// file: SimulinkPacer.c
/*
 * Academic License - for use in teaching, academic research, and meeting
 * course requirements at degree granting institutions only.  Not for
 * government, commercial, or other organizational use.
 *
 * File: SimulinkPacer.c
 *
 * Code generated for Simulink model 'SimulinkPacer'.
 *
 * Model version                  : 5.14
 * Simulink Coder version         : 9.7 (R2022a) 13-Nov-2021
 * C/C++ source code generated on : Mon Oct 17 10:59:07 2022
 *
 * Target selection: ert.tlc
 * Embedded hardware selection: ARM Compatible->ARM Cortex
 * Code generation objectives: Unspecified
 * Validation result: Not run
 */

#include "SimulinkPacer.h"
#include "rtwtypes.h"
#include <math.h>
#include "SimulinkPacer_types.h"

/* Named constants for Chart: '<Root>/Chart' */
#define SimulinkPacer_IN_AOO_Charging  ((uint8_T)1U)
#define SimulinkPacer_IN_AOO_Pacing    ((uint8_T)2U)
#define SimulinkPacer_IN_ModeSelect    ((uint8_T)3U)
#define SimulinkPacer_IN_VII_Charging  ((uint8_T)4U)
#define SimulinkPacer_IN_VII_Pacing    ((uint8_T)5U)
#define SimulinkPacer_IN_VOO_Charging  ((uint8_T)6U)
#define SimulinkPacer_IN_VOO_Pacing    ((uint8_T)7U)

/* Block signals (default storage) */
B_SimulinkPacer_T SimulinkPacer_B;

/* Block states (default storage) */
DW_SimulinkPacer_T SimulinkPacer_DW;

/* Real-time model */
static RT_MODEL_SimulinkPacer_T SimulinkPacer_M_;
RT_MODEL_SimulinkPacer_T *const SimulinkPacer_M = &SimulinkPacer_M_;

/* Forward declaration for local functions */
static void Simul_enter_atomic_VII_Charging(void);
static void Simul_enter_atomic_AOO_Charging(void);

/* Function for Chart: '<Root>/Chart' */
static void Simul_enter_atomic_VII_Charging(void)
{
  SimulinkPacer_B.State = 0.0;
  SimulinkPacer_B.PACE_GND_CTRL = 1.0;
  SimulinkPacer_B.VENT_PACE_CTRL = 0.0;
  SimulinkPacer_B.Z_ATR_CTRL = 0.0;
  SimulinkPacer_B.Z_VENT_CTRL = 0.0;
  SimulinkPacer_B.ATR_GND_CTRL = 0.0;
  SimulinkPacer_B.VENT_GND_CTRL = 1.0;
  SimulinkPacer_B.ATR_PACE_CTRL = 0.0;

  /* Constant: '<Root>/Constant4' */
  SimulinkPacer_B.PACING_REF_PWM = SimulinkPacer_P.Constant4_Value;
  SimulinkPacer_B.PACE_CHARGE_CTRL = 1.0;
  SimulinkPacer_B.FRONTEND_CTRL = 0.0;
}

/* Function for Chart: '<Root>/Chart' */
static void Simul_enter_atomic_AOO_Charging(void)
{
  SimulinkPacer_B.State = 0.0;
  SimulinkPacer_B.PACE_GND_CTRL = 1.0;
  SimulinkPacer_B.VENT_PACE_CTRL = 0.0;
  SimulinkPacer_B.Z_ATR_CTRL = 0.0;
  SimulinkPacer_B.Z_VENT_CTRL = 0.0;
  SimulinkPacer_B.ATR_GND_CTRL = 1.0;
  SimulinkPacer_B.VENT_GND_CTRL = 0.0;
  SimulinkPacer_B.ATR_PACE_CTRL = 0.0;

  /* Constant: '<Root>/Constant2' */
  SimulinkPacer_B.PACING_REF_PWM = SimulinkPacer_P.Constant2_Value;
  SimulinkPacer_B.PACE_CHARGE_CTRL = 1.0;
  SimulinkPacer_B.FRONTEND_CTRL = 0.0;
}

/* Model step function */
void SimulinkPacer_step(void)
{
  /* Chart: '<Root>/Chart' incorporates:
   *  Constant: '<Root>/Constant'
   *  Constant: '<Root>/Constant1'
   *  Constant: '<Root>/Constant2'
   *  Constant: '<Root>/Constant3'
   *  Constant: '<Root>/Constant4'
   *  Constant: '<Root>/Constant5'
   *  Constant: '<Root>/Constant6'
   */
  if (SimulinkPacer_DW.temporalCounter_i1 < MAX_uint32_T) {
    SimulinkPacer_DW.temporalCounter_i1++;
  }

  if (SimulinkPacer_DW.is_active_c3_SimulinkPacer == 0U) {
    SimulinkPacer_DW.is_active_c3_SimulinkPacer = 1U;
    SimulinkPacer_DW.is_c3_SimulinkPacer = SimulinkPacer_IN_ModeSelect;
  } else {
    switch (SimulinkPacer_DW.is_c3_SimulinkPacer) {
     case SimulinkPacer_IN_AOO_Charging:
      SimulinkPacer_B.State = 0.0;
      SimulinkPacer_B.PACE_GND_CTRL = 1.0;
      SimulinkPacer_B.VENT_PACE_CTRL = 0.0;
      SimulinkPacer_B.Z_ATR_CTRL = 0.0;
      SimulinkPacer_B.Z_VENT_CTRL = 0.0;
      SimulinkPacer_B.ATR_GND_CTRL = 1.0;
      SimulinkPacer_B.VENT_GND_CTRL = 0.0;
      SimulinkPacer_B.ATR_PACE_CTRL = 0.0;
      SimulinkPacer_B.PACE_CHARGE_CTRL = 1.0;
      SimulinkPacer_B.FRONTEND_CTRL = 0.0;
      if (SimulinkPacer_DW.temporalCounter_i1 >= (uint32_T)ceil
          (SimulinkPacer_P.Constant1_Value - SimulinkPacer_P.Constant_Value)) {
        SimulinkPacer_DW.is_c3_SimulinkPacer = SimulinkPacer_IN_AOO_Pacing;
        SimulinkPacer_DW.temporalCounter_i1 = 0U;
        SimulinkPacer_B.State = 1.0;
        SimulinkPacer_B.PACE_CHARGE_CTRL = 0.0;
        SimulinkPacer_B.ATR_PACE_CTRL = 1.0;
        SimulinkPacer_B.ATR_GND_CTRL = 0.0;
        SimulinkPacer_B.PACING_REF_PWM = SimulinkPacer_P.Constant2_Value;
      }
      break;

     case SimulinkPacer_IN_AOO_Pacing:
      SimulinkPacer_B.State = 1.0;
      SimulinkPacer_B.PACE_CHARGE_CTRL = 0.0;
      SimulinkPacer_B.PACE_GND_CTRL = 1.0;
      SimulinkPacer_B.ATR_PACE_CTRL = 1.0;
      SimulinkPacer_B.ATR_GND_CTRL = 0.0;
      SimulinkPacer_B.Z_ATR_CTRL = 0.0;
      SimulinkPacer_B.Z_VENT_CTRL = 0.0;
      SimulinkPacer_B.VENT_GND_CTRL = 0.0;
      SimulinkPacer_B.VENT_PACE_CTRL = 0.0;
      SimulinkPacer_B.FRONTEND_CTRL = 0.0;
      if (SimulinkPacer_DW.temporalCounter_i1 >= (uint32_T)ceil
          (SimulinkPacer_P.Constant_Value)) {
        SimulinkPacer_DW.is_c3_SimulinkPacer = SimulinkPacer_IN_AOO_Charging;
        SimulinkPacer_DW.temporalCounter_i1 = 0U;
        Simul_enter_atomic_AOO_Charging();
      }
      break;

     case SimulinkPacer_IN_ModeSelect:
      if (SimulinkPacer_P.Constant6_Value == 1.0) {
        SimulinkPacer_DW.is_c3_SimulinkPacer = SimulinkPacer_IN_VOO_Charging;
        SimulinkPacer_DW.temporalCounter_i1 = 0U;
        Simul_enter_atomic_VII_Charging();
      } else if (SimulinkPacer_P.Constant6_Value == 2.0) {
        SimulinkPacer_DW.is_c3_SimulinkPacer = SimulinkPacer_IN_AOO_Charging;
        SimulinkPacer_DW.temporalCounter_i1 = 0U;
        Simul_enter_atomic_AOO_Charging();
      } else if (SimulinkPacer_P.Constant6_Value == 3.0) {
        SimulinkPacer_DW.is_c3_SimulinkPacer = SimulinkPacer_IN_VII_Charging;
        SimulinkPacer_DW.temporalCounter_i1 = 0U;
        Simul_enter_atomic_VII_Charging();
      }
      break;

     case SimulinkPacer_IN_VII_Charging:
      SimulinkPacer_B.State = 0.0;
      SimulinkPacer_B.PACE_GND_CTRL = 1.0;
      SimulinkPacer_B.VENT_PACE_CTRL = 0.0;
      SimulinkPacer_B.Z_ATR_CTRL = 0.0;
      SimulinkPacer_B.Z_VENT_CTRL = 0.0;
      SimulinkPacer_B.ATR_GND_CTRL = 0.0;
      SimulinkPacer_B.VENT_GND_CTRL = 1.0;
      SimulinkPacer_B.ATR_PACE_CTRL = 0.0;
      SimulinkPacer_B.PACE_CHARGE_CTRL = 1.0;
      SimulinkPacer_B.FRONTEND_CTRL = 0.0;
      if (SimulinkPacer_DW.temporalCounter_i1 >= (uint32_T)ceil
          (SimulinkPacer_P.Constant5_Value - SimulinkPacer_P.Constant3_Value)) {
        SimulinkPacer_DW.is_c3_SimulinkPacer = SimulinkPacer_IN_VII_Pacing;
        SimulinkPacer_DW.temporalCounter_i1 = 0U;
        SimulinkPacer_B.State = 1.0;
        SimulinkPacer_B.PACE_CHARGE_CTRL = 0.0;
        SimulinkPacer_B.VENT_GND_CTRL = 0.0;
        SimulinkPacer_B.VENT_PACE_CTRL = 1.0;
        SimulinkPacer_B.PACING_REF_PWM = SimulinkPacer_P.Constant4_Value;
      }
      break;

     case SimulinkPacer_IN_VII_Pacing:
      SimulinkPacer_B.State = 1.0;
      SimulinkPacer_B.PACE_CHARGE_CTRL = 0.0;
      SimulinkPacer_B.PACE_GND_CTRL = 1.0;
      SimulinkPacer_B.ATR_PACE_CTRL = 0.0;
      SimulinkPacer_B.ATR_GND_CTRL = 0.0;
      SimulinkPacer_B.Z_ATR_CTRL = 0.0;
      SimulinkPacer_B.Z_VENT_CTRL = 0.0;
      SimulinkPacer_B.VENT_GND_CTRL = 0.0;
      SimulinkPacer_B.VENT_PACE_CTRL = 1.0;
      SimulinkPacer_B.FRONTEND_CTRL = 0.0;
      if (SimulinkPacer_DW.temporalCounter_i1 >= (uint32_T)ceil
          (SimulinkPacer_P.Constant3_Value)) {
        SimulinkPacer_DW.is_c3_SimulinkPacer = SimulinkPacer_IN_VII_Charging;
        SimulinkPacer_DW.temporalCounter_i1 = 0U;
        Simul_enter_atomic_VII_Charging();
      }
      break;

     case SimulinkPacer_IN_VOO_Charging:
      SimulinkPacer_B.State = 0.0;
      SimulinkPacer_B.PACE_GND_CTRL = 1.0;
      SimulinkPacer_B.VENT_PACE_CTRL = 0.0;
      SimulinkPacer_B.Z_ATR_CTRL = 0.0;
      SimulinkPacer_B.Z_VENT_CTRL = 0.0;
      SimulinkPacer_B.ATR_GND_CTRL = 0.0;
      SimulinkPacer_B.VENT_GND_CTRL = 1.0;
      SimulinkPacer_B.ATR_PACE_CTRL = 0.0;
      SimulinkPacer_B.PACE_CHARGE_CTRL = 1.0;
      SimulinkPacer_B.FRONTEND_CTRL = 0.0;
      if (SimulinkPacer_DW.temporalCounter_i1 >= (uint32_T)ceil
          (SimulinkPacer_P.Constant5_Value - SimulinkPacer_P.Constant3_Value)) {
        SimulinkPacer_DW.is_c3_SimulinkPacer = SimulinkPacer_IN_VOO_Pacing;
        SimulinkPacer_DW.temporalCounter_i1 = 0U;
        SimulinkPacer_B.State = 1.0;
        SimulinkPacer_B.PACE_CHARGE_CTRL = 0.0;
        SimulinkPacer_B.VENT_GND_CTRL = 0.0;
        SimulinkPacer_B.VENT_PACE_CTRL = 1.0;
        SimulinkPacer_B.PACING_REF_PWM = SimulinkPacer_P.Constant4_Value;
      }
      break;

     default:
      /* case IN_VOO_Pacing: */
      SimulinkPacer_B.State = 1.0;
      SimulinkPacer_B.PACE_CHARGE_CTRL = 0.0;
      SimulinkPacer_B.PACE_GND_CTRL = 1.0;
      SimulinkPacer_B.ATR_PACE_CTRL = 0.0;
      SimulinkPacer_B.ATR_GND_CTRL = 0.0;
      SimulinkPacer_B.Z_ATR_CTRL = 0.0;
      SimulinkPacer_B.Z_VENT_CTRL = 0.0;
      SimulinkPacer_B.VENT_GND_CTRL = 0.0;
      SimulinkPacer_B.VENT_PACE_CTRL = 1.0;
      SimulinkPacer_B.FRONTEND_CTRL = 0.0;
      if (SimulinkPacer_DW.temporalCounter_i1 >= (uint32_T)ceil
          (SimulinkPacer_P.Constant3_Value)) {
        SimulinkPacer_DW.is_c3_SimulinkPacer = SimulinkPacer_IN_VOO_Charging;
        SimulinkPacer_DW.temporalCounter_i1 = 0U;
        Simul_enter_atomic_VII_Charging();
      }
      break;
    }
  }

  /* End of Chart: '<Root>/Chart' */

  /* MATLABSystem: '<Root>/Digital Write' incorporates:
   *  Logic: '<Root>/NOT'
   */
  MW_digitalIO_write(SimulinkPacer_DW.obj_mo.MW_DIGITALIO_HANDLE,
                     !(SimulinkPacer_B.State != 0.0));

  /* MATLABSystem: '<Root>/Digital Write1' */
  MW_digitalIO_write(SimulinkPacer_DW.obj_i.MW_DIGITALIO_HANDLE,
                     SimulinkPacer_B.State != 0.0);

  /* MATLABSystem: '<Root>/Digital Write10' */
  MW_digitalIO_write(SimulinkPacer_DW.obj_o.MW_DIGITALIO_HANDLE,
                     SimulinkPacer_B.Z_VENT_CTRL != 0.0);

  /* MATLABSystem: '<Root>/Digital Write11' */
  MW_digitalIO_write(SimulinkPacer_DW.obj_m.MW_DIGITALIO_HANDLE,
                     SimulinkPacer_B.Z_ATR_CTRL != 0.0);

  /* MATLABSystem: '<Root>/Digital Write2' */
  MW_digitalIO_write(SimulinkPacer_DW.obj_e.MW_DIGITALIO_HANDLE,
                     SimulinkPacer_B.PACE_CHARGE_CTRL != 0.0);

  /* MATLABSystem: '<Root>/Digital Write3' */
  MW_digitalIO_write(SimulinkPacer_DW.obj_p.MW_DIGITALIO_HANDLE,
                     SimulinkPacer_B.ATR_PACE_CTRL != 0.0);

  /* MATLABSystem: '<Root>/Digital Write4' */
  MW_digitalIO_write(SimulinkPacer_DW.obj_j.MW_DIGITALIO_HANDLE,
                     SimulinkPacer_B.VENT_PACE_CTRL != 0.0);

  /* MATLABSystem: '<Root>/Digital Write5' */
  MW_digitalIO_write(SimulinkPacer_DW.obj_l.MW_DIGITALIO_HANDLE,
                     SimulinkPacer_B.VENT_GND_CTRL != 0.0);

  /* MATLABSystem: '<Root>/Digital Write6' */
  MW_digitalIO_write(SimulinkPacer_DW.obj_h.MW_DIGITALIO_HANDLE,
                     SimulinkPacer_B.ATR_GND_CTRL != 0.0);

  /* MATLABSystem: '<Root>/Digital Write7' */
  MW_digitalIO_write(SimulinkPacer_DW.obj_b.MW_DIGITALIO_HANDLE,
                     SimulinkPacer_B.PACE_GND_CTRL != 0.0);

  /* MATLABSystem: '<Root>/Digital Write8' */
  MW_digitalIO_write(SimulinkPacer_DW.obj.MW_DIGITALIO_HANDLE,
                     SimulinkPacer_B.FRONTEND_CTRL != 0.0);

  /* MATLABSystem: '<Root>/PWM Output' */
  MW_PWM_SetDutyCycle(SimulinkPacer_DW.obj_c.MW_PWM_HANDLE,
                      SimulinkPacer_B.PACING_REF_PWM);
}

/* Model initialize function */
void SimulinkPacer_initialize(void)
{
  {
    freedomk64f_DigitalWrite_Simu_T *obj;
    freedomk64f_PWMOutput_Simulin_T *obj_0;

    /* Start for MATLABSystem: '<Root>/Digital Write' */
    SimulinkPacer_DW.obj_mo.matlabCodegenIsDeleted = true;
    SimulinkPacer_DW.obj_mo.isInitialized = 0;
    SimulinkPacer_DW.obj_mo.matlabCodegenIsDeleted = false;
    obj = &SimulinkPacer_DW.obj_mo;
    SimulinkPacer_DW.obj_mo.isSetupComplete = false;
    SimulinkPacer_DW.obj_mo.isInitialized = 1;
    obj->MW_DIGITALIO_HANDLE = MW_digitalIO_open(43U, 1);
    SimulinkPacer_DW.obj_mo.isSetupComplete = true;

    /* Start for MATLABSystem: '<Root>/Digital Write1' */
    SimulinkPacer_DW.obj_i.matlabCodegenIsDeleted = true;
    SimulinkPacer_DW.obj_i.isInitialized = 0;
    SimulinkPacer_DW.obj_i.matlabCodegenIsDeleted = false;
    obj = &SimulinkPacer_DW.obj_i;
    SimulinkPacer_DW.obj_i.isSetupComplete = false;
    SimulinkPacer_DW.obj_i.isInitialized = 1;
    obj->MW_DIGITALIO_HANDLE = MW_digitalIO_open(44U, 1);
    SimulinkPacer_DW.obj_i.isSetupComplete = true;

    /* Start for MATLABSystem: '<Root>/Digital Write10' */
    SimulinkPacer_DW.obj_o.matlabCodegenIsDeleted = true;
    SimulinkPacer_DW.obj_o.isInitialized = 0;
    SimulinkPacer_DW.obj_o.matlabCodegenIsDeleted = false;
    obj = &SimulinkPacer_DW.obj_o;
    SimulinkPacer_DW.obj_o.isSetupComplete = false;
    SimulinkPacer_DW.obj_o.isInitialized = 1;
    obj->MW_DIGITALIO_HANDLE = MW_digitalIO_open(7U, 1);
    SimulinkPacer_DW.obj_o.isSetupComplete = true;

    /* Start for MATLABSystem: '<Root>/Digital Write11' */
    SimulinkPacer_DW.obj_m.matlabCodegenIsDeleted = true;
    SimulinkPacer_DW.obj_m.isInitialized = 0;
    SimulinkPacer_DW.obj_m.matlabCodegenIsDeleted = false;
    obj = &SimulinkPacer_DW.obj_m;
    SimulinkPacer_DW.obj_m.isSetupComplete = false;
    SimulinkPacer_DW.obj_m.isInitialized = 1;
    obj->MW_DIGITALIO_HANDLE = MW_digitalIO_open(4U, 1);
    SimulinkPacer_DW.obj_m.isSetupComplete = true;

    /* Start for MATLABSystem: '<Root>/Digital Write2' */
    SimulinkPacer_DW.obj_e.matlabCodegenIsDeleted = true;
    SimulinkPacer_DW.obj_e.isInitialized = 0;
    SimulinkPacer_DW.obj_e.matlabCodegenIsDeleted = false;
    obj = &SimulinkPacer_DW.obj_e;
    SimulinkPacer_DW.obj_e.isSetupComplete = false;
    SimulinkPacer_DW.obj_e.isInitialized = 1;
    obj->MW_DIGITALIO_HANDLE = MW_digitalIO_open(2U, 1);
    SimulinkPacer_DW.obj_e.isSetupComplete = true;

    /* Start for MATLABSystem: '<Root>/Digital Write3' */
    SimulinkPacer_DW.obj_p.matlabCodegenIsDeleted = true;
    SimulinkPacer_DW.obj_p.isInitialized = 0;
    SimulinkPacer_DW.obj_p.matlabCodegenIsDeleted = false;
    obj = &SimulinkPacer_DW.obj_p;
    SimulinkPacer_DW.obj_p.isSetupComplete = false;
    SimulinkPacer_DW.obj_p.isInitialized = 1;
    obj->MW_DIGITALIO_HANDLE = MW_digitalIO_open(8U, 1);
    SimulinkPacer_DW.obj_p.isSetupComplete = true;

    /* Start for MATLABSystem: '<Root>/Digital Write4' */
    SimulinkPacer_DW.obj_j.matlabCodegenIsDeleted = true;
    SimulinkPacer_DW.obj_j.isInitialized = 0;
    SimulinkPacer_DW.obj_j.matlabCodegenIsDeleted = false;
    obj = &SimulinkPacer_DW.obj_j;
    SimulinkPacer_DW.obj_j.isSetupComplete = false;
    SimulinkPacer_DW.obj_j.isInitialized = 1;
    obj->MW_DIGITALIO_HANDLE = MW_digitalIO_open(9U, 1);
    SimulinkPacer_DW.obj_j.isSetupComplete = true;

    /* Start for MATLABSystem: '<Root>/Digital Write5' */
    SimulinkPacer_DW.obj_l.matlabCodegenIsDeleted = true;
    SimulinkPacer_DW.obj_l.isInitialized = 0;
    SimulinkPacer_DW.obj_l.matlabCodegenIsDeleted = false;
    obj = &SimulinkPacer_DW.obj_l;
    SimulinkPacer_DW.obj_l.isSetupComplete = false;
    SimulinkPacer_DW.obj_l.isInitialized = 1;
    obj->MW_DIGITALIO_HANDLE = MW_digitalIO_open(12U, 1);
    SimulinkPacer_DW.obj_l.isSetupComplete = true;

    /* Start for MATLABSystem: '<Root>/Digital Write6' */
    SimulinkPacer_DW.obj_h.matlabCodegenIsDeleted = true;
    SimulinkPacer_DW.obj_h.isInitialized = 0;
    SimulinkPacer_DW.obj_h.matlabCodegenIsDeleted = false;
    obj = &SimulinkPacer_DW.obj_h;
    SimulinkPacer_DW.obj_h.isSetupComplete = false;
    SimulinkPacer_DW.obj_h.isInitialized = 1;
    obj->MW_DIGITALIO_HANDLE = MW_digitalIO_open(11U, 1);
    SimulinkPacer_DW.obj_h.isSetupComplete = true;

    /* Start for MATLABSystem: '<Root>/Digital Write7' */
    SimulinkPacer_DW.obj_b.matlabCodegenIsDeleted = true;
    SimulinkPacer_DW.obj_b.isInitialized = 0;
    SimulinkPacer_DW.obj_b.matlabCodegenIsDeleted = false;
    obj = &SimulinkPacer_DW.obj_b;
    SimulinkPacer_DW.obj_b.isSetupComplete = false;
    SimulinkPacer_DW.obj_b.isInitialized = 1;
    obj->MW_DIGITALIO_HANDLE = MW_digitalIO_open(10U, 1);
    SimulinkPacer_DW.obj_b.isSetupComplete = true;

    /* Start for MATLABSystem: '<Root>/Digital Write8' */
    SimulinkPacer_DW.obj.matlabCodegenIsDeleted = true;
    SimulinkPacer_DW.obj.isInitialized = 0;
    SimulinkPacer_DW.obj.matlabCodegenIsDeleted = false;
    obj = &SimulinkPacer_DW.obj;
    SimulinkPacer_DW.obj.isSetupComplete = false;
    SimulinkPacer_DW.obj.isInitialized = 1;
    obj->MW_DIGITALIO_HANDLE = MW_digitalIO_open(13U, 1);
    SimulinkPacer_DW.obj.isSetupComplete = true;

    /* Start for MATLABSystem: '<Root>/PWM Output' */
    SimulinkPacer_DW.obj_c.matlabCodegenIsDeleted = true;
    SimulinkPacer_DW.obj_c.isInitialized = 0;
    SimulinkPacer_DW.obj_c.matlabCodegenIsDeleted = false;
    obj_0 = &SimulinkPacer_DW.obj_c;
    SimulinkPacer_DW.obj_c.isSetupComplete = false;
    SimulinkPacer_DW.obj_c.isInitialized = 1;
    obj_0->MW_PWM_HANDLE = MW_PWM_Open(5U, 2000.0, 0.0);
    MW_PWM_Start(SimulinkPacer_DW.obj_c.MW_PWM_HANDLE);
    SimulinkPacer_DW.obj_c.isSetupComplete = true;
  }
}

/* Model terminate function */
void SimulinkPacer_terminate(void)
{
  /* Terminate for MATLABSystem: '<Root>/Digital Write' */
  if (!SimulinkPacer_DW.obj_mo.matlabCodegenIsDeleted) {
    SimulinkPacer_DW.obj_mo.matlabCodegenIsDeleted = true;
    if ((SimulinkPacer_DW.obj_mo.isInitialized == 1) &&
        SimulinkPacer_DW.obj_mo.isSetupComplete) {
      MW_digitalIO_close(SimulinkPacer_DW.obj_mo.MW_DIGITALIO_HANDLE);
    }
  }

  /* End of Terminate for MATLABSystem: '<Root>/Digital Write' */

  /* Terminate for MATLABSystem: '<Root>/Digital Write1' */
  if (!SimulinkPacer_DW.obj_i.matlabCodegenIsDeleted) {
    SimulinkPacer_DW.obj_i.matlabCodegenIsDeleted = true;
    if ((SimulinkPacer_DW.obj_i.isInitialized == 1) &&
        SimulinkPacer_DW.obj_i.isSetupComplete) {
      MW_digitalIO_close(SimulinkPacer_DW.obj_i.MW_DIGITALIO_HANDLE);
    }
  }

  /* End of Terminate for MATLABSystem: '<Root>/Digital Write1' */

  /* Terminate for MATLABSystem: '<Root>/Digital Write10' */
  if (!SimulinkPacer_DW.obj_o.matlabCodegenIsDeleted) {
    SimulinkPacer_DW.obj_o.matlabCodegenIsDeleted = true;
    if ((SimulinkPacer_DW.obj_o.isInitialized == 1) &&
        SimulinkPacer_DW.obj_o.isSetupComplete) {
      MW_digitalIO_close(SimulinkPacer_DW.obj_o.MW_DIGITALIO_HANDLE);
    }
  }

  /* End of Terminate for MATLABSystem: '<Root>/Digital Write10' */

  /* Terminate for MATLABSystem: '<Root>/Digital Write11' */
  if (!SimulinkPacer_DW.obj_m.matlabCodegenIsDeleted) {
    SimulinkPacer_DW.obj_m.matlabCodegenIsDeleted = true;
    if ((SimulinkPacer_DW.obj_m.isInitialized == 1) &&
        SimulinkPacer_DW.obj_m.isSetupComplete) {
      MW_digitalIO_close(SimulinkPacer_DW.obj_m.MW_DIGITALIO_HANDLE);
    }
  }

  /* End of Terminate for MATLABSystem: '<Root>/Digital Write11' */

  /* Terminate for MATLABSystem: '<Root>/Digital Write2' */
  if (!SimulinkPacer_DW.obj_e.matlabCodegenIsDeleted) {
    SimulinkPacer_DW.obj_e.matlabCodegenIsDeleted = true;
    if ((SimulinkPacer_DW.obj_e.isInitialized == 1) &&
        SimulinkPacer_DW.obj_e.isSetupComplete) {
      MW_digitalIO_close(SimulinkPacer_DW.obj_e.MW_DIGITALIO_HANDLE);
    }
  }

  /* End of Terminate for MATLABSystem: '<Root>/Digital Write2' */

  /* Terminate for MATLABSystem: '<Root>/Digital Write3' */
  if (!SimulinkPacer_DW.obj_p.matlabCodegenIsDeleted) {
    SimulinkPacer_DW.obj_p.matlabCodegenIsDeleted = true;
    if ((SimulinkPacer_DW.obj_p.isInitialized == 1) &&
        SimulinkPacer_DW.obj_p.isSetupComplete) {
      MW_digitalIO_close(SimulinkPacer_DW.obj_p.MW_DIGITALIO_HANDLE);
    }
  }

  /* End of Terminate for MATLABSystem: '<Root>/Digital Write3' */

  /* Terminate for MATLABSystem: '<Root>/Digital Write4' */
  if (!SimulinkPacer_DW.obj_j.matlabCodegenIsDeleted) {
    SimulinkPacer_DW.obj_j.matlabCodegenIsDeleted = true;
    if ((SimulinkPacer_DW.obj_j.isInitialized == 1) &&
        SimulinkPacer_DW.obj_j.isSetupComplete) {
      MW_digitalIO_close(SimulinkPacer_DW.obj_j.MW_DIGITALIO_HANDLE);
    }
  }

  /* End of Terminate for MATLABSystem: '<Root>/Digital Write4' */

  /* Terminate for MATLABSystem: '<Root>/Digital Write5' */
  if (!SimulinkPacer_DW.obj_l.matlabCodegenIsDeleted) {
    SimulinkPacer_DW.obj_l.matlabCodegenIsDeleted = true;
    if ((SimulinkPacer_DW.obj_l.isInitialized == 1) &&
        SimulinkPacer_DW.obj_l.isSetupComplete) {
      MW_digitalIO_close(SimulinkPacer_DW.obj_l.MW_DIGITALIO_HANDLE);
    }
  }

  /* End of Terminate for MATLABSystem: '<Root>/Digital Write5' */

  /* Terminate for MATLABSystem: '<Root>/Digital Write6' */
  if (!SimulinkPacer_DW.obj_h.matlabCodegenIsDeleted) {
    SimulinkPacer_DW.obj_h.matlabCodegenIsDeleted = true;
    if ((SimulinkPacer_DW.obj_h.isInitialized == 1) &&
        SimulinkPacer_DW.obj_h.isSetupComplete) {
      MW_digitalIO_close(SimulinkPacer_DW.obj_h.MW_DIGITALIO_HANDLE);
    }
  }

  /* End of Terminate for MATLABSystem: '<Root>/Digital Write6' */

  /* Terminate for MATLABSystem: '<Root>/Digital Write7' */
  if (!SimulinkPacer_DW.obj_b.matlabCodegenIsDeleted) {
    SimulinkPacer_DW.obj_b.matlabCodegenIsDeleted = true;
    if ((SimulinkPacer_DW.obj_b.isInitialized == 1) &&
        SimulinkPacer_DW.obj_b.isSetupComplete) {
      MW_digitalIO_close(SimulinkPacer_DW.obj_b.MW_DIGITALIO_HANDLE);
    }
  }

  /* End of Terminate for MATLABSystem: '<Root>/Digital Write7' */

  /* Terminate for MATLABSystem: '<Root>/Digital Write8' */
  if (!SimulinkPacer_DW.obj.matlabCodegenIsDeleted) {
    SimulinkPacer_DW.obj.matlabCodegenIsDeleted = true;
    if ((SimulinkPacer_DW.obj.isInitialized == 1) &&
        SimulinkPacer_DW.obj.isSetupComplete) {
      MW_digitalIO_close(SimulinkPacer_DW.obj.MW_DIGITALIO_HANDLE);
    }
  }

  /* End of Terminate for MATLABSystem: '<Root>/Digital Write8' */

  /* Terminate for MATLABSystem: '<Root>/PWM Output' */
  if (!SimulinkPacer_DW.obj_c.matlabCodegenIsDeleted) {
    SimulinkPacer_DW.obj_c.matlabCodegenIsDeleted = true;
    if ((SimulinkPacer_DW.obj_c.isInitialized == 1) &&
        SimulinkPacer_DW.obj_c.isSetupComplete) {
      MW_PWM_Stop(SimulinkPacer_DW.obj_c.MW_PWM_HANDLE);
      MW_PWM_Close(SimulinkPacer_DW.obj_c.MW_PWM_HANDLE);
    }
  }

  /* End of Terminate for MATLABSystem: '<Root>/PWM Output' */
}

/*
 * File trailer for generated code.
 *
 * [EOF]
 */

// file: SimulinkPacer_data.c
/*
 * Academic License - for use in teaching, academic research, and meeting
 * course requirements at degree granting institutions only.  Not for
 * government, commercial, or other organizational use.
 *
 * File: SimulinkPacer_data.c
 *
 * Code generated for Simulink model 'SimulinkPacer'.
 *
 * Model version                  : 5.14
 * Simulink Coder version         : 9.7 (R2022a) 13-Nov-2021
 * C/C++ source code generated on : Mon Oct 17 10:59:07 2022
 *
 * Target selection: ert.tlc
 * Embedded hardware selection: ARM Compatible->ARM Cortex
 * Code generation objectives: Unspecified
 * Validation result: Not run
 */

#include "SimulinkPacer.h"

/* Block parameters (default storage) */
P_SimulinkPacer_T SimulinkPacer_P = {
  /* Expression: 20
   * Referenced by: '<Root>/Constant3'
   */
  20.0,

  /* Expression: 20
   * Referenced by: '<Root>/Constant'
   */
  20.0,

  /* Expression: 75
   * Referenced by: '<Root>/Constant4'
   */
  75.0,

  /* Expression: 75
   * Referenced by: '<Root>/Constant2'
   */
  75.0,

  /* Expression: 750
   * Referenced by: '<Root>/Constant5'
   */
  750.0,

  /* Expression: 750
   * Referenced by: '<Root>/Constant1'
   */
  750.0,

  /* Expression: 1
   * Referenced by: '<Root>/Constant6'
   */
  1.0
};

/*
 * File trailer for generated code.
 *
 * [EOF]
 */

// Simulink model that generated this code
simulink model "SimulinkPacer"  (R2022a)
settings: Solver=FixedStepAuto  StartTime=0.0  StopTime=10.0  FixedStep=1e-3  RelTol=1e-3  EnableMultiTasking=on
undefined symbols (not defined in the file): D10, D11, D12, D13, D2, D4, D5, D7, D8, D9, PTA0, PTA2, PTB23, PTB9, PTC3, PTC4, PTD0, PTD1, PTD2, PTD3
libraries: frdmk64flib x12

== system SimulinkPacer ==
  Chart : Stateflow chart  TreatAsAtomicUnit=on
  Constant : Constant  Value=20
  Constant1 : Constant  Value=750
  Constant2 : Constant  Value=75
  Constant3 : Constant  Value=20
  Constant4 : Constant  Value=75
  Constant5 : Constant  Value=750
  Constant6 : Constant
  Digital Write : frdmk64flib/Digital Write  Whichpin=GREEN_LED
  Digital Write1 : frdmk64flib/Digital Write  Whichpin=BLUE_LED
  Digital Write10 : frdmk64flib/Digital Write  Whichpin=PTC3 (D7)
  Digital Write11 : frdmk64flib/Digital Write  Whichpin=PTB23 (D4)
  Digital Write2 : frdmk64flib/Digital Write  Whichpin=PTB9 (D2)
  Digital Write3 : frdmk64flib/Digital Write  Whichpin=PTA0 (D8)
  Digital Write4 : frdmk64flib/Digital Write  Whichpin=PTC4 (D9)
  Digital Write5 : frdmk64flib/Digital Write  Whichpin=PTD3 (D12)
  Digital Write6 : frdmk64flib/Digital Write  Whichpin=PTD2 (D11)
  Digital Write7 : frdmk64flib/Digital Write  Whichpin=PTD0 (D10)
  Digital Write8 : frdmk64flib/Digital Write  Whichpin=PTD1 (D13)
  NOT : Logic  Operator=NOT  IconShape=distinctive  AllPortsSameDT=off  OutDataTypeStr=boolean
  PWM Output : frdmk64flib/PWM Output  Whichpin=PTA2 (D5)  InitialFrequency=2000  InitialDutyCycle=0
  wires:
  Constant/1 -> Chart/2(atr_pw)
  Constant1/1 -> Chart/6(atr_pr)
  Constant2/1 -> Chart/4(atr_amp)
  Constant3/1 -> Chart/1(vent_pw)
  Constant4/1 -> Chart/3(vent_amp)
  NOT/1 -> Digital Write/1
  Chart/2(PACE_CHARGE_CTRL) -> Digital Write2/1
  Chart/3(VENT_PACE_CTRL) -> Digital Write4/1
  Chart/4(ATR_PACE_CTRL) -> Digital Write3/1
  Chart/6(ATR_GND_CTRL) -> Digital Write6/1
  Chart/8(FRONTEND_CTRL) -> Digital Write8/1
  Chart/7(PACE_GND_CTRL) -> Digital Write7/1
  Chart/9(PACING_REF_PWM) -> PWM Output/1
  Constant5/1 -> Chart/5(vent_pr)
  Chart/1(State) -> Digital Write1/1, NOT/1
  Chart/5(VENT_GND_CTRL) -> Digital Write5/1
  Chart/10(Z_ATR_CTRL) -> Digital Write11/1
  Chart/11(Z_VENT_CTRL) -> Digital Write10/1
  Constant6/1 -> Chart/7(Mode)

== stateflow chart SimulinkPacer/Chart ==
  state VOO_Pacing
    entry:
    State = 1
    PACE_CHARGE_CTRL = 0
    PACE_GND_CTRL = 1
    ATR_PACE_CTRL = 0
    ATR_GND_CTRL = 0
    Z_ATR_CTRL = 0
    Z_VENT_CTRL = 0
    VENT_GND_CTRL = 0
    VENT_PACE_CTRL = 1
    FRONTEND_CTRL = 0
    PACING_REF_PWM = vent_amp
  state VOO_Charging
    entry:
    State = 0
    PACE_GND_CTRL = 1
    VENT_PACE_CTRL = 0
    Z_ATR_CTRL = 0
    Z_VENT_CTRL = 0
    ATR_GND_CTRL = 0
    VENT_GND_CTRL = 1
    ATR_PACE_CTRL = 0
    PACING_REF_PWM = vent_amp
    PACE_CHARGE_CTRL = 1
    FRONTEND_CTRL = 0
  state ModeSelect
  state AOO_Pacing
    entry:
    State = 1
    PACE_CHARGE_CTRL = 0
    PACE_GND_CTRL = 1
    ATR_PACE_CTRL = 1
    ATR_GND_CTRL = 0
    Z_ATR_CTRL = 0
    Z_VENT_CTRL = 0
    VENT_GND_CTRL = 0
    VENT_PACE_CTRL = 0
    FRONTEND_CTRL = 0
    PACING_REF_PWM = atr_amp
  state AOO_Charging
    entry:
    State = 0
    PACE_GND_CTRL = 1
    VENT_PACE_CTRL = 0
    Z_ATR_CTRL = 0
    Z_VENT_CTRL = 0
    ATR_GND_CTRL = 1
    VENT_GND_CTRL = 0
    ATR_PACE_CTRL = 0
    PACING_REF_PWM = atr_amp
    PACE_CHARGE_CTRL = 1
    FRONTEND_CTRL = 0
  state VII_Pacing
    entry:
    State = 1
    PACE_CHARGE_CTRL = 0
    PACE_GND_CTRL = 1
    ATR_PACE_CTRL = 0
    ATR_GND_CTRL = 0
    Z_ATR_CTRL = 0
    Z_VENT_CTRL = 0
    VENT_GND_CTRL = 0
    VENT_PACE_CTRL = 1
    FRONTEND_CTRL = 0
    PACING_REF_PWM = vent_amp
  state VII_Charging
    entry:
    State = 0
    PACE_GND_CTRL = 1
    VENT_PACE_CTRL = 0
    Z_ATR_CTRL = 0
    Z_VENT_CTRL = 0
    ATR_GND_CTRL = 0
    VENT_GND_CTRL = 1
    ATR_PACE_CTRL = 0
    PACING_REF_PWM = vent_amp
    PACE_CHARGE_CTRL = 1
    FRONTEND_CTRL = 0
  (default) -> ModeSelect
  ModeSelect -> VOO_Charging [order 1] : [Mode == 1]
  VOO_Pacing -> VOO_Charging : [after(vent_pw, msec)]
  ModeSelect -> VII_Charging [order 3] : [Mode == 3]
  ModeSelect -> AOO_Charging [order 2] : [Mode == 2]
  VOO_Charging -> VOO_Pacing : [after(vent_pr - vent_pw, msec)]
  AOO_Pacing -> AOO_Charging : [after(atr_pw, msec)]
  AOO_Charging -> AOO_Pacing : [after(atr_pr - atr_pw, msec)]
  VII_Pacing -> VII_Charging : [after(vent_pw, msec)]
  VII_Charging -> VII_Pacing : [after(vent_pr - vent_pw, msec)]
  data: vent_pw input; atr_pw input; vent_amp input; atr_amp input; vent_pr input; atr_pr input; State output double =0; PACE_CHARGE_CTRL output; VENT_PACE_CTRL output; ATR_PACE_CTRL output; VENT_GND_CTRL output; ATR_GND_CTRL output; PACE_GND_CTRL output; FRONTEND_CTRL output; PACING_REF_PWM output; Z_ATR_CTRL output; Z_VENT_CTRL output; Mode input
